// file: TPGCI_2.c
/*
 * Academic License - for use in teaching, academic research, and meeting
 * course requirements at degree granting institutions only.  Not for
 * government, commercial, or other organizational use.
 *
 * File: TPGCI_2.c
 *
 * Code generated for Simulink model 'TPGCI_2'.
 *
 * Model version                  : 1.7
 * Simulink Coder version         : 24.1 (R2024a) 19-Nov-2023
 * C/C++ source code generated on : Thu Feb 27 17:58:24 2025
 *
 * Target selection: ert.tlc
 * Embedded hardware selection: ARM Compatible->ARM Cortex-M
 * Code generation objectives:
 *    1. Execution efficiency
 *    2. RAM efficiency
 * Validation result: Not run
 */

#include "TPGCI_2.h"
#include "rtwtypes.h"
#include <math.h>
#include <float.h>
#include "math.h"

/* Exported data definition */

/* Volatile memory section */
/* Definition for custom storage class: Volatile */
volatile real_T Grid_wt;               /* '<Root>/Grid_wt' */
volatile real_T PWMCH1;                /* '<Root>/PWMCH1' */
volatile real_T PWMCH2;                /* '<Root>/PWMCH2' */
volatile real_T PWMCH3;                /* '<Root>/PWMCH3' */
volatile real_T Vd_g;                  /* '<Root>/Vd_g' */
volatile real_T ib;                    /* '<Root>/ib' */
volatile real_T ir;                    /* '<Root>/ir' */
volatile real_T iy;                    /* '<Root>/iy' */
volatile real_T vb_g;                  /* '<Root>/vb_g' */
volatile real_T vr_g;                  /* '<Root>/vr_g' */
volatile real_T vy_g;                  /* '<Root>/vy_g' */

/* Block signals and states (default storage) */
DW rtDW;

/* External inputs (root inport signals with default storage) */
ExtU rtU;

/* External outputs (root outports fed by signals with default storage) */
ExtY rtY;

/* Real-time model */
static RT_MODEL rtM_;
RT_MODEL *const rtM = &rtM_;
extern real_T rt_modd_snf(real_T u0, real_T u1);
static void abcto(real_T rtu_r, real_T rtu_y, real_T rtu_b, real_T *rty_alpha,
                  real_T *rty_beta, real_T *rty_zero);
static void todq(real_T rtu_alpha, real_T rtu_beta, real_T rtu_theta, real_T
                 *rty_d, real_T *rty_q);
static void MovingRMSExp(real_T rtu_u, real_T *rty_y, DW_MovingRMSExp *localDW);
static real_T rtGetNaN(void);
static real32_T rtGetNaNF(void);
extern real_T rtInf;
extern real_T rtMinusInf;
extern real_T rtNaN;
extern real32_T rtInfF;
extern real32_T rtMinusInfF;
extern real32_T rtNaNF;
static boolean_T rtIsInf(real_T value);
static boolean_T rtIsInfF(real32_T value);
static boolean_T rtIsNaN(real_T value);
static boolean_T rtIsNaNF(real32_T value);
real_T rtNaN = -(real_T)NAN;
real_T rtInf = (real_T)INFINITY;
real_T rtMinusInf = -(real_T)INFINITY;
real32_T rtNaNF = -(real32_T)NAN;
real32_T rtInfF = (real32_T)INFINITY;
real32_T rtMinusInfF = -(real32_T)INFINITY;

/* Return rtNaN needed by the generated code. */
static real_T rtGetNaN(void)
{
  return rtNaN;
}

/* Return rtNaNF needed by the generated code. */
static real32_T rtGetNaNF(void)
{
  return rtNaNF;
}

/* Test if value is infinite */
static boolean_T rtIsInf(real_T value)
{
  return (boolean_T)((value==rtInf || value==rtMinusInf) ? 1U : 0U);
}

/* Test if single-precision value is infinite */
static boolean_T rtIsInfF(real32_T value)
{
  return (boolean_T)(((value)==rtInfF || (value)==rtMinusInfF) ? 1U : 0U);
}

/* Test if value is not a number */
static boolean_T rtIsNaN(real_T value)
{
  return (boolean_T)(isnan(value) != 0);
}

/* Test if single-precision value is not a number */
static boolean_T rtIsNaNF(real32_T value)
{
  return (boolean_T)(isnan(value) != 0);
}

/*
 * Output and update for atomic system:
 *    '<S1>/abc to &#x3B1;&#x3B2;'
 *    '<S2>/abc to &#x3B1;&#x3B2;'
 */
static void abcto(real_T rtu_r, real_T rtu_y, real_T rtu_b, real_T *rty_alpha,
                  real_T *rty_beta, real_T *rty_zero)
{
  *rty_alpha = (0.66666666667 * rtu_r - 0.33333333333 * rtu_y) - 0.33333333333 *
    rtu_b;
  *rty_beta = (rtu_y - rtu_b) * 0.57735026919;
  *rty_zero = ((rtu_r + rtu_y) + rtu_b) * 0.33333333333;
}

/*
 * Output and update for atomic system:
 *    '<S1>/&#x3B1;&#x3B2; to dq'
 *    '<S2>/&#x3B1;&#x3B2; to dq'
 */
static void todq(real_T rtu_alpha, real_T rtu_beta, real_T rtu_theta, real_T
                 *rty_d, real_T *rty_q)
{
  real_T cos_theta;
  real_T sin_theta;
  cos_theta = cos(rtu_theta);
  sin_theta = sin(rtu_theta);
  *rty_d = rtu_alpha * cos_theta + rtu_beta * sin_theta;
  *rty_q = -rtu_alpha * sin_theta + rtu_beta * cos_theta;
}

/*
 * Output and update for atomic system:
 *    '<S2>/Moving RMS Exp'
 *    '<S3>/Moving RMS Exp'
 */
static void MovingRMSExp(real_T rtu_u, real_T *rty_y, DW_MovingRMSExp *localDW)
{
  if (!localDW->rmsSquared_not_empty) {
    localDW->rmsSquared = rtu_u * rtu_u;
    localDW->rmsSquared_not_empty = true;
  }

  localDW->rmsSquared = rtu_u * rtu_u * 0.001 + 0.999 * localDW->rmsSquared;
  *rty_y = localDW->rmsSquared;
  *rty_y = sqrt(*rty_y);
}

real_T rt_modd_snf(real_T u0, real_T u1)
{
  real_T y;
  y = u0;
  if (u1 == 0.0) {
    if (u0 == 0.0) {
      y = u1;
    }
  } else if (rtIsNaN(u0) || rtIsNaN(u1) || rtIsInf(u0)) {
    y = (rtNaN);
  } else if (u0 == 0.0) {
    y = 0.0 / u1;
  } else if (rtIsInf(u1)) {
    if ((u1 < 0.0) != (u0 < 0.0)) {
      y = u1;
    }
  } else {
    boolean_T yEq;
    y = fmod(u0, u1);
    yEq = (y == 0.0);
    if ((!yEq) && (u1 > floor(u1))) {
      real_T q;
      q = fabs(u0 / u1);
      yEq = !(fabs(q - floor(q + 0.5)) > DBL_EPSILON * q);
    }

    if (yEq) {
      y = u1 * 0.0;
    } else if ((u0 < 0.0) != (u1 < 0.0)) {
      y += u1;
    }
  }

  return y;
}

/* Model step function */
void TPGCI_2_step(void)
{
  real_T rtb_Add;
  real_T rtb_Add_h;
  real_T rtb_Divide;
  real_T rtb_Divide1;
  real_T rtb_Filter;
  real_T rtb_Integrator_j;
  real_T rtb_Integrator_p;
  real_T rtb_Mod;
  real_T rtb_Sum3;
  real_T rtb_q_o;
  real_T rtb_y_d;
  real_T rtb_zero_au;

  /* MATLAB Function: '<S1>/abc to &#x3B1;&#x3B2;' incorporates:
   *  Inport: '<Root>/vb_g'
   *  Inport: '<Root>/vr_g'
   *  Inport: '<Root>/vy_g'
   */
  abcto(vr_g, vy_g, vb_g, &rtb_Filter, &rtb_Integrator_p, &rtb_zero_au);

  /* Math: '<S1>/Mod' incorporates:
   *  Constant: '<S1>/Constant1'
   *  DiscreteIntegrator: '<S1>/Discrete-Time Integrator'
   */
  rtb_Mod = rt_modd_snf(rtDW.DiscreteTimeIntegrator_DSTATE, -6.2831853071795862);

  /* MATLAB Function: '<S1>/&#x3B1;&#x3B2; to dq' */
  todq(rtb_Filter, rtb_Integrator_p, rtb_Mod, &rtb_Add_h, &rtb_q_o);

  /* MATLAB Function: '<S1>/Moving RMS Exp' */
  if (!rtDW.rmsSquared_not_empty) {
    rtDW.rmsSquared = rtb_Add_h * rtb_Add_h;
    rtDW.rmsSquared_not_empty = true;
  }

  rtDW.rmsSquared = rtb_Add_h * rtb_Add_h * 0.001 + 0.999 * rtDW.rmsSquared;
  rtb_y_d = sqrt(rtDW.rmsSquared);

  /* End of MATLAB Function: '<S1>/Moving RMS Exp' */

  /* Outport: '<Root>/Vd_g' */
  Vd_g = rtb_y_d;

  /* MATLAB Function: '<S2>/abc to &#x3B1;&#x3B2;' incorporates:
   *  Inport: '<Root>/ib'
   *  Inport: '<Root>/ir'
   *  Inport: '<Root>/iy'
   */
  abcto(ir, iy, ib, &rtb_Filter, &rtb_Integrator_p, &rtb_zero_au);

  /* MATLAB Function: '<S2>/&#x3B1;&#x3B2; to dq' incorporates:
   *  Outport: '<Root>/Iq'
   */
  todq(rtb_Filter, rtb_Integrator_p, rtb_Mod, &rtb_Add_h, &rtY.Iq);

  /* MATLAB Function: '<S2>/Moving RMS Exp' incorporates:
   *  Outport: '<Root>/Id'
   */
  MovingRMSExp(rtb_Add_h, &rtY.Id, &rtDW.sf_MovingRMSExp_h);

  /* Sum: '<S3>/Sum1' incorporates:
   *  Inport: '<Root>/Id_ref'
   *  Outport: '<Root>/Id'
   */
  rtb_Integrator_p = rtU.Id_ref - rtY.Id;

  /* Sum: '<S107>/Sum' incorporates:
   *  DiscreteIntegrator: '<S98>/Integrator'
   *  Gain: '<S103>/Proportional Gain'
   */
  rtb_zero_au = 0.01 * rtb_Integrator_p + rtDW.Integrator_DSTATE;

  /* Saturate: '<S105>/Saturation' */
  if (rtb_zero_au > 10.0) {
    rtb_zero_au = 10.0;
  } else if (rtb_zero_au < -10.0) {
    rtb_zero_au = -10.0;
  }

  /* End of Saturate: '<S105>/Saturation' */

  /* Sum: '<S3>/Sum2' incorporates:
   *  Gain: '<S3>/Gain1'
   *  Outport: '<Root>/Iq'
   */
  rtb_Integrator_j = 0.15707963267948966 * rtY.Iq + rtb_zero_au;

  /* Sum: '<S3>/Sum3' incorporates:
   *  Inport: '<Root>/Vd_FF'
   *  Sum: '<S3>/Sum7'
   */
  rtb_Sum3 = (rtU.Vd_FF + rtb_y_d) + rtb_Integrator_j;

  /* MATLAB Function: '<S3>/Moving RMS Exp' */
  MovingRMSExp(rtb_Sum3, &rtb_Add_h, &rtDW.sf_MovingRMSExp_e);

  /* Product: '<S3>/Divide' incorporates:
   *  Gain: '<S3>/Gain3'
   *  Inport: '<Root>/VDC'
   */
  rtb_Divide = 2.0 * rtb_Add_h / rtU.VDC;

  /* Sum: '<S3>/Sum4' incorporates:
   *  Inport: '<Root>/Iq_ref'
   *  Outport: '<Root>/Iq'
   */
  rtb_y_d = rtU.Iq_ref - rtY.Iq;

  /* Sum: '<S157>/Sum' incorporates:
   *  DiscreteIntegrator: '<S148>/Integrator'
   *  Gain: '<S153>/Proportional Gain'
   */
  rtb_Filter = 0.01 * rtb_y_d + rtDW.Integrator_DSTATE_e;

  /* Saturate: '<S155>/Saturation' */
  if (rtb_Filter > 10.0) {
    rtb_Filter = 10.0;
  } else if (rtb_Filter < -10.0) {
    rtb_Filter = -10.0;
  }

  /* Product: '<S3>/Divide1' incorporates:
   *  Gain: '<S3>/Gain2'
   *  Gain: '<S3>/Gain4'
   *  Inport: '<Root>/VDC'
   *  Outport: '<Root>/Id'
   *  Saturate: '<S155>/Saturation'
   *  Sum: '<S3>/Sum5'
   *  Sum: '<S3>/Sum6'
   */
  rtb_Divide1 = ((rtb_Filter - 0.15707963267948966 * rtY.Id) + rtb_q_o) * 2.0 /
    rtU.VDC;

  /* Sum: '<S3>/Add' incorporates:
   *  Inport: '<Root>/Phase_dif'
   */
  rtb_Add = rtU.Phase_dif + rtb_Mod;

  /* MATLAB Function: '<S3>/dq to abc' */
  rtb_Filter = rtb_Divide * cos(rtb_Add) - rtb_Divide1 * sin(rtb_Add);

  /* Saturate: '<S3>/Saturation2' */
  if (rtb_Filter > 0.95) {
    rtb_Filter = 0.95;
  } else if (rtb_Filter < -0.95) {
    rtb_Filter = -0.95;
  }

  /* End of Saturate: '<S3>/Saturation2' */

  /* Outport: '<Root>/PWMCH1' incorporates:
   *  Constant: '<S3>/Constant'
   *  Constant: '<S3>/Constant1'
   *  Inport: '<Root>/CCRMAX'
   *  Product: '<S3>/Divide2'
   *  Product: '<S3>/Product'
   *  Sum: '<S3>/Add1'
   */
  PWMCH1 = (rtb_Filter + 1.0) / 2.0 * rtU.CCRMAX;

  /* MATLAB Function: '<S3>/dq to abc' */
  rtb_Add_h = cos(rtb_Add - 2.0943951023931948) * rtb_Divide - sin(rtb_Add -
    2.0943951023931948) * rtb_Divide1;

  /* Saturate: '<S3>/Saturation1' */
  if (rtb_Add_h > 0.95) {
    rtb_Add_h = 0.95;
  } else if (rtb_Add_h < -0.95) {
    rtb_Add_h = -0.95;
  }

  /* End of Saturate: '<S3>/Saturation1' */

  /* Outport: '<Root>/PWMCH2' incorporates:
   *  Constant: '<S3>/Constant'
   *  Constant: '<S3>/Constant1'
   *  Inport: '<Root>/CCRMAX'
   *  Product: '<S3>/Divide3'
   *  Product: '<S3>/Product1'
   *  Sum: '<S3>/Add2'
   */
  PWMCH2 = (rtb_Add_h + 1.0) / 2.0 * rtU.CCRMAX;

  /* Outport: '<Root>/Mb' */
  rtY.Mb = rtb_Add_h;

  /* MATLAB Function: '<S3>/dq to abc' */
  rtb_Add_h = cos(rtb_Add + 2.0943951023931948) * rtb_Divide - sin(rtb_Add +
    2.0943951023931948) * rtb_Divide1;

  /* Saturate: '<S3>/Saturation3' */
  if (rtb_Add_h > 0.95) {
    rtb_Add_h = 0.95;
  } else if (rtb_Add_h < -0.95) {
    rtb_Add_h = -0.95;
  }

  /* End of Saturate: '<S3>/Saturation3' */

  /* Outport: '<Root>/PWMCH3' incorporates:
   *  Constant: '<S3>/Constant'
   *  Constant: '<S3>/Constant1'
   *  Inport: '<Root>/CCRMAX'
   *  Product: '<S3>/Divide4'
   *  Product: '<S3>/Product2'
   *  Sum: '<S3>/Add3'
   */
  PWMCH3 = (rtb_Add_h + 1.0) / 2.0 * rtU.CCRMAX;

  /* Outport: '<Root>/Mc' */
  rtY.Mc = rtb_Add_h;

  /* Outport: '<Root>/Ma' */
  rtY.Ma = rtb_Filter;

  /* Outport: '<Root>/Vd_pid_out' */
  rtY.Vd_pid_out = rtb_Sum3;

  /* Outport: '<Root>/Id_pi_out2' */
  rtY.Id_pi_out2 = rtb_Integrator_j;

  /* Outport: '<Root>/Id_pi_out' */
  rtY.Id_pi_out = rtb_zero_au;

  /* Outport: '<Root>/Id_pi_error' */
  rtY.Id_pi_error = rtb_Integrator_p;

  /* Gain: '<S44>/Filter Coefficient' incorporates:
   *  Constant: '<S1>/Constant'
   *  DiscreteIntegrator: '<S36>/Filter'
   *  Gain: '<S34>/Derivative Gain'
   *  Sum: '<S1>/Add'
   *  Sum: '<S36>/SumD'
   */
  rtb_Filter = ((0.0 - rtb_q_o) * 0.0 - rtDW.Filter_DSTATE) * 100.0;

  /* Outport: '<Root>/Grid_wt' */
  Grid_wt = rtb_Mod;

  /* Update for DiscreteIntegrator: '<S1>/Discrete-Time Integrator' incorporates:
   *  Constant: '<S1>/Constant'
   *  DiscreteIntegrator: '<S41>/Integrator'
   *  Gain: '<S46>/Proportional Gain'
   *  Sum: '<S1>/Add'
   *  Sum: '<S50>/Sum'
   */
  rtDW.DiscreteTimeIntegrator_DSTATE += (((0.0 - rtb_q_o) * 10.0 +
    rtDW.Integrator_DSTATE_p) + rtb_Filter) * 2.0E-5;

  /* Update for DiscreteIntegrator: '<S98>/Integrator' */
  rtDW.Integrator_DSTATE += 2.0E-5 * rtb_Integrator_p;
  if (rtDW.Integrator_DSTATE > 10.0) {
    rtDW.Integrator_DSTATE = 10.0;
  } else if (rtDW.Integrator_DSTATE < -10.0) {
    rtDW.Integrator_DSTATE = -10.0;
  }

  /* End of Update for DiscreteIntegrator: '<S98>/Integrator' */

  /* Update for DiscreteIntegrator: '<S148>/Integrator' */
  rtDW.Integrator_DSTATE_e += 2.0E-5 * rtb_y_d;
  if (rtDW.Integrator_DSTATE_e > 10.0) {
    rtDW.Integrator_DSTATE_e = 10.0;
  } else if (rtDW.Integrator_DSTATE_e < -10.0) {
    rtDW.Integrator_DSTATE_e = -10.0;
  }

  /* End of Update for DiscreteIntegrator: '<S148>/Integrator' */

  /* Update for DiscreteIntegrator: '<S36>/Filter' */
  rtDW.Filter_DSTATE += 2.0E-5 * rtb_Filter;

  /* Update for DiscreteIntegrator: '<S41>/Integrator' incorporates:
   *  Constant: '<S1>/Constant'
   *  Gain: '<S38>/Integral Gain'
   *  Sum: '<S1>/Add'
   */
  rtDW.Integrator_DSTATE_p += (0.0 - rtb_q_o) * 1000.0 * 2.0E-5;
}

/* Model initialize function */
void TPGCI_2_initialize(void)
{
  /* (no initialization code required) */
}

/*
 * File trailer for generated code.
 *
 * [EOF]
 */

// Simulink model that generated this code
simulink model "TPGCI_2"  (R2024a)
settings: Solver=FixedStepDiscrete  StartTime=0.0  StopTime=10.0  FixedStep=2e-5  RelTol=1e-3
undefined symbols (not defined in the file): DiscIntNeverNeededParam
libraries: slpidlib x3

== system TPGCI_2 ==
  vr_g : Inport
  vy_g : Inport  Port=2
  vb_g : Inport  Port=3
  ir : Inport  Port=4
  iy : Inport  Port=5
  ib : Inport  Port=6
  Id_ref : Inport  Port=7
  Iq_ref : Inport  Port=8
  VDC : Inport  Port=9
  Phase_dif : Inport  Port=10
  Vd_FF : Inport  Port=11
  CCRMAX : Inport  Port=12
  Phase locked loop : Subsystem
  Subsystem : Subsystem
  Subsystem1 : Subsystem
  Vd_g : Outport
  Grid_wt : Outport  Port=2
  Id : Outport  Port=3
  Iq : Outport  Port=4
  PWMCH1 : Outport  Port=5
  PWMCH2 : Outport  Port=6
  PWMCH3 : Outport  Port=7
  Ma : Outport  Port=8
  Mb : Outport  Port=9
  Mc : Outport  Port=10
  Vd_pid_out : Outport  Port=11
  Id_pi_error : Outport  Port=12
  Id_pi_out : Outport  Port=13
  Id_pi_out2 : Outport  Port=14
  wires:
  Iq_ref/1 -> Subsystem1/2(Iq_ref)
  Vd_FF/1 -> Subsystem1/5(Vd_FF)
  Subsystem/1(Id) -> Id/1
  VDC/1 -> Subsystem1/3(VDC)
  vy_g/1 -> Phase locked loop/2(vy_g)
  Phase locked loop/2(wt) -> Grid_wt/1
  ir/1 -> Subsystem/1(r)
  ib/1 -> Subsystem/3(b)
  vb_g/1 -> Phase locked loop/3(vb_g)
  Phase_dif/1 -> Subsystem1/4(Phase_dif)
  iy/1 -> Subsystem/2(y)
  Id_ref/1 -> Subsystem1/1(Id_ref)
  vr_g/1 -> Phase locked loop/1(vr_g)
  Subsystem/2(Iq) -> Iq/1
  Phase locked loop/1(Vd_g) -> Vd_g/1
  CCRMAX/1 -> Subsystem1/6(CCRMAX)
  Subsystem1/1(Vd_pid_out) -> Vd_pid_out/1
  Subsystem1/2(Id_pi_error) -> Id_pi_error/1
  Subsystem1/3(Id_pi_out) -> Id_pi_out/1
  Subsystem1/4(Id_pi_out2) -> Id_pi_out2/1
  Subsystem1/5(PWMCH1) -> PWMCH1/1
  Subsystem1/6(PWMCH2) -> PWMCH2/1
  Subsystem1/7(PWMCH3) -> PWMCH3/1
  Subsystem1/8(Ma) -> Ma/1
  Subsystem1/9(Mb) -> Mb/1
  Subsystem1/10(Mc) -> Mc/1

== system TPGCI_2/Phase locked loop ==
  vr_g : Inport
  vy_g : Inport  Port=2
  vb_g : Inport  Port=3
  Add : Sum  Inputs=+-
  Constant : Constant  Value=0
  Constant1 : Constant  Value=-2*pi
  Discrete-Time Integrator : DiscreteIntegrator  SampleTime=2e-5  ICPrevOutput=DiscIntNeverNeededParam  ICPrevScaledInput=DiscIntNeverNeededParam
  Mod : Math  Operator=mod
  Moving RMS Exp : MATLAB Function  TreatAsAtomicUnit=on
  PID Controller : slpidlib/PID Controller  Controller=PID  Form=Parallel  TimeDomain=Discrete-time  UseExternalTs=off  SampleTime=2e-5  IntegratorMethod=Forward Euler  FilterMethod=Forward Euler  ControllerParametersSource=internal  P=10  I=1000  UseKiTs=off  D=0  UseExternalDerivativeSource=off  N=100  UseFilter=on  TunerSelectOption=Transfer Function Based (PID Tuner App)  InitialConditionSource=internal  InitialConditionForIntegrator=0  InitialConditionForFilter=0  DifferentiatorICPrevScaledInput=0  ExternalReset=none  TrackingMode=off  Kt=1  LimitOutput=off  SatLimitsSource=internal  UpperSaturationLimit=inf  LowerSaturationLimit=-inf  LinearizeAsGain=on  AntiWindupMode=none  Kb=1  LimitIntegrator=off  UpperIntegratorSaturationLimit=inf  LowerIntegratorSaturationLimit=-inf  POutMin=[]  POutMax=[]  IOutMin=[]  IOutMax=[]  DOutMin=[]  DOutMax=[]  NOutMin=[]  NOutMax=[]  SumOutMin=[]  SumOutMax=[]  SaturationOutMin=[]  SaturationOutMax=[]  PParamMin=[]  PParamMax=[]  IParamMin=[]  IParamMax=[]  DParamMin=[]  DParamMax=[]  NParamMin=[]  NParamMax=[]  KbParamMin=[]  KbParamMax=[]  KtParamMin=[]  KtParamMax=[]  KbOutMin=[]  KbOutMax=[]  KtOutMin=[]  KtOutMax=[]  IntegratorOutMin=[]  IntegratorOutMax=[]  FilterOutMin=[]  FilterOutMax=[]  SumI1OutMin=[]  SumI1OutMax=[]  SumI2OutMin=[]  SumI2OutMax=[]  SumI3OutMin=[]  SumI3OutMax=[]  SumI4OutMin=[]  SumI4OutMax=[]  SumDOutMin=[]  SumDOutMax=[]  DifferentiatorOutMin=[]  DifferentiatorOutMax=[]  FilterDiffOutCoefMin=[]  FilterDiffOutCoefMax=[]  ReciprocalOutMin=[]  ReciprocalOutMax=[]  SumDenOutMin=[]  SumDenOutMax=[]  SumNumOutMin=[]  SumNumOutMax=[]  DivideOutMin=[]  DivideOutMax=[]  UdiffTsProdOutMin=[]  UdiffTsProdOutMax=[]  NTsProdOutMin=[]  NTsProdOutMax=[]  UintegralTsProdOutMin=[]  UintegralTsProdOutMax=[]  UngainTsProdOutMin=[]  UngainTsProdOutMax=[]  ClampingZeroOutDataTypeStr=Inherit: Inherit via back propagation  ClampingZeroOutMin=[]  ClampingZeroOutMax=[]  FilterDenConstantOutDataTypeStr=Inherit: Inherit via back propagation  FilterDenConstantOutMin=[]  FilterDenConstantOutMax=[]  PCopyOutDataTypeStr=Inherit: Inherit via back propagation  PCopyOutMin=[]  PCopyOutMax=[]  NCopyOutDataTypeStr=Inherit: Inherit via back propagation  NCopyOutMin=[]  NCopyOutMax=[]  IntegratorContinuousStateAttributes=''  IntegratorStateMustResolveToSignalObject=off  IntegratorRTWStateStorageClass=Auto  FilterContinuousStateAttributes=''  FilterStateMustResolveToSignalObject=off  FilterRTWStateStorageClass=Auto  ParallelPVariant=InternalParameters  IdealPVariant=Disabled  IVariant=InternalParameters  DVariant=InternalParameters  IntegratorVariant=Discrete  SatVariant=Disabled  AWVariant=Passthrough  PCopyVariant=Disabled  TRVariant=Disabled  FdbkBlocksVariant=Forward  IdealPFdbkVariant=Disabled  SatFdbkVariant=Disabled  DerivativeFilterVariant=ForwardEulerFilter  NVariant=InternalParameters  NCopyVariant=Disabled  FilterICVariant=InternalICsFilter  IntegratorICVariant=InternalICs  ExternalResetVariant=Disabled  TRSumVariant=Passthrough  SumFdbkVariant=Disabled  SumVariant=Sum_PID  TsampFilterVariant=InternalTs  TsampNgainVariant=Passthrough  TsampIntegralVariant=Disabled_SignalSpec  ExternalSaturationOutDataTypeStr=Inherit: Same as second input  DerivativeSourceVariant=ErrorSignal
  Terminator1 : Terminator
  abc to αβ : MATLAB Function  TreatAsAtomicUnit=on
  αβ to dq : MATLAB Function  TreatAsAtomicUnit=on
  Vd_g : Outport
  wt : Outport  Port=2
  tag scope: Vd_g=global, Vq_g=global, wt=global
  wires:
  αβ to dq/3(zero) -> Terminator1/1
  abc to αβ/2(beta) -> αβ to dq/2(beta)
  αβ to dq/1(d) -> Moving RMS Exp/1(u)
  [wt] -> αβ to dq/4(theta)
  abc to αβ/1(alpha) -> αβ to dq/1(alpha)
  abc to αβ/3(zero) -> αβ to dq/3("zero ")
  Mod/1 -> wt/1, [wt]
  Discrete-Time Integrator/1 -> Mod/1
  Constant1/1 -> Mod/2
  Constant/1 -> Add/1
  αβ to dq/2(q) -> [Vq_g], Add/2
  PID Controller/1 -> Discrete-Time Integrator/1
  Add/1 -> PID Controller/1
  vy_g/1 -> abc to αβ/2(y)
  vb_g/1 -> abc to αβ/3(b)
  vr_g/1 -> abc to αβ/1(r)
  Moving RMS Exp/1(y) -> [Vd_g], Vd_g/1

== system TPGCI_2/Subsystem ==
  r : Inport
  y : Inport  Port=2
  b : Inport  Port=3
  Moving RMS Exp : MATLAB Function  TreatAsAtomicUnit=on
  Terminator1 : Terminator
  abc to αβ : MATLAB Function  TreatAsAtomicUnit=on
  αβ to dq : MATLAB Function  TreatAsAtomicUnit=on
  Id : Outport
  Iq : Outport  Port=2
  tag scope: Id_i=global, Iq_i=global
  wires:
  abc to αβ/2(beta) -> αβ to dq/2(beta)
  αβ to dq/1(d) -> Moving RMS Exp/1(u)
  αβ to dq/2(q) -> Iq/1, [Iq_i]
  abc to αβ/1(alpha) -> αβ to dq/1(alpha)
  abc to αβ/3(zero) -> αβ to dq/3("zero ")
  αβ to dq/3(zero) -> Terminator1/1
  Moving RMS Exp/1(y) -> Id/1, [Id_i]
  [wt] -> αβ to dq/4(theta)
  y/1 -> abc to αβ/2(y)
  b/1 -> abc to αβ/3(b)
  r/1 -> abc to αβ/1(r)

== system TPGCI_2/Subsystem1 ==
  note: Iq Reference
  note: Id Reference
  Id_ref : Inport
  Iq_ref : Inport  Port=2
  VDC : Inport  Port=3
  Phase_dif : Inport  Port=4
  Vd_FF : Inport  Port=5
  CCRMAX : Inport  Port=6
  Add{,1..3} (4 alike) : Sum
  Constant : Constant
  Constant1 : Constant  Value=2  VectorParams1D=off  SampleTime=-1
  Divide{,1..4} (5 alike) : Product  Inputs=*/
  Gain1 : Gain  Gain=2*pi*50*500e-6
  Gain2 : Gain  Gain=2*pi*50*500e-6
  Gain3 : Gain  Gain=2
  Gain4 : Gain  Gain=2
  Moving RMS Exp : MATLAB Function  TreatAsAtomicUnit=on
  PID Controller1 : slpidlib/PID Controller  Controller=PI  Form=Parallel  TimeDomain=Discrete-time  UseExternalTs=off  SampleTime=2e-5  IntegratorMethod=Forward Euler  FilterMethod=Forward Euler  ControllerParametersSource=internal  P=0.01  I=1  UseKiTs=off  D=0  UseExternalDerivativeSource=off  N=100  UseFilter=on  TunerSelectOption=Transfer Function Based (PID Tuner App)  InitialConditionSource=internal  InitialConditionForIntegrator=0  InitialConditionForFilter=0  DifferentiatorICPrevScaledInput=0  ExternalReset=none  TrackingMode=off  Kt=1  LimitOutput=on  SatLimitsSource=internal  UpperSaturationLimit=+10  LowerSaturationLimit=-10  LinearizeAsGain=on  AntiWindupMode=none  Kb=1  LimitIntegrator=on  UpperIntegratorSaturationLimit=+10  LowerIntegratorSaturationLimit=-10  RndMeth=Nearest  POutMin=[]  POutMax=[]  IOutMin=[]  IOutMax=[]  DOutMin=[]  DOutMax=[]  NOutMin=[]  NOutMax=[]  SumOutMin=[]  SumOutMax=[]  SaturationOutMin=[]  SaturationOutMax=[]  PParamMin=[]  PParamMax=[]  IParamMin=[]  IParamMax=[]  DParamMin=[]  DParamMax=[]  NParamMin=[]  NParamMax=[]  KbParamMin=[]  KbParamMax=[]  KtParamMin=[]  KtParamMax=[]  KbOutMin=[]  KbOutMax=[]  KtOutMin=[]  KtOutMax=[]  IntegratorOutMin=[]  IntegratorOutMax=[]  FilterOutMin=[]  FilterOutMax=[]  SumI1OutMin=[]  SumI1OutMax=[]  SumI2OutMin=[]  SumI2OutMax=[]  SumI3OutMin=[]  SumI3OutMax=[]  SumI4OutMin=[]  SumI4OutMax=[]  SumDOutMin=[]  SumDOutMax=[]  DifferentiatorOutMin=[]  DifferentiatorOutMax=[]  FilterDiffOutCoefMin=[]  FilterDiffOutCoefMax=[]  ReciprocalOutMin=[]  ReciprocalOutMax=[]  SumDenOutMin=[]  SumDenOutMax=[]  SumNumOutMin=[]  SumNumOutMax=[]  DivideOutMin=[]  DivideOutMax=[]  UdiffTsProdOutMin=[]  UdiffTsProdOutMax=[]  NTsProdOutMin=[]  NTsProdOutMax=[]  UintegralTsProdOutMin=[]  UintegralTsProdOutMax=[]  UngainTsProdOutMin=[]  UngainTsProdOutMax=[]  ClampingZeroOutDataTypeStr=Inherit: Inherit via back propagation  ClampingZeroOutMin=[]  ClampingZeroOutMax=[]  FilterDenConstantOutDataTypeStr=Inherit: Inherit via back propagation  FilterDenConstantOutMin=[]  FilterDenConstantOutMax=[]  PCopyOutDataTypeStr=Inherit: Inherit via back propagation  PCopyOutMin=[]  PCopyOutMax=[]  NCopyOutDataTypeStr=Inherit: Inherit via back propagation  NCopyOutMin=[]  NCopyOutMax=[]  IntegratorContinuousStateAttributes=''  IntegratorStateMustResolveToSignalObject=off  IntegratorRTWStateStorageClass=Auto  FilterContinuousStateAttributes=''  FilterStateMustResolveToSignalObject=off  FilterRTWStateStorageClass=Auto  ParallelPVariant=InternalParameters  IdealPVariant=Disabled  IVariant=InternalParameters  DVariant=Disabled  IntegratorVariant=Discrete  SatVariant=Enabled  AWVariant=Passthrough  PCopyVariant=Disabled  TRVariant=Disabled  FdbkBlocksVariant=Forward  IdealPFdbkVariant=Disabled  SatFdbkVariant=Disabled  DerivativeFilterVariant=Disabled  NVariant=Disabled  NCopyVariant=Disabled_SignalSpec  FilterICVariant=Disabled  IntegratorICVariant=InternalICs  ExternalResetVariant=Disabled  TRSumVariant=Passthrough  SumFdbkVariant=Disabled  SumVariant=Sum_PI  TsampFilterVariant=InternalTs  TsampNgainVariant=Passthrough  TsampIntegralVariant=Disabled_SignalSpec  ExternalSaturationOutDataTypeStr=Inherit: Same as second input  DerivativeSourceVariant=Disabled
  PID Controller2 : slpidlib/PID Controller  Controller=PI  Form=Parallel  TimeDomain=Discrete-time  UseExternalTs=off  SampleTime=2e-5  IntegratorMethod=Forward Euler  FilterMethod=Forward Euler  ControllerParametersSource=internal  P=0.01  I=1  UseKiTs=off  D=0  UseExternalDerivativeSource=off  N=100  UseFilter=on  TunerSelectOption=Transfer Function Based (PID Tuner App)  InitialConditionSource=internal  InitialConditionForIntegrator=0  InitialConditionForFilter=0  DifferentiatorICPrevScaledInput=0  ExternalReset=none  TrackingMode=off  Kt=1  LimitOutput=on  SatLimitsSource=internal  UpperSaturationLimit=10  LowerSaturationLimit=-10  LinearizeAsGain=on  AntiWindupMode=none  Kb=1  LimitIntegrator=on  UpperIntegratorSaturationLimit=10  LowerIntegratorSaturationLimit=-10  POutMin=[]  POutMax=[]  IOutMin=[]  IOutMax=[]  DOutMin=[]  DOutMax=[]  NOutMin=[]  NOutMax=[]  SumOutMin=[]  SumOutMax=[]  SaturationOutMin=[]  SaturationOutMax=[]  PParamMin=[]  PParamMax=[]  IParamMin=[]  IParamMax=[]  DParamMin=[]  DParamMax=[]  NParamMin=[]  NParamMax=[]  KbParamMin=[]  KbParamMax=[]  KtParamMin=[]  KtParamMax=[]  KbOutMin=[]  KbOutMax=[]  KtOutMin=[]  KtOutMax=[]  IntegratorOutMin=[]  IntegratorOutMax=[]  FilterOutMin=[]  FilterOutMax=[]  SumI1OutMin=[]  SumI1OutMax=[]  SumI2OutMin=[]  SumI2OutMax=[]  SumI3OutMin=[]  SumI3OutMax=[]  SumI4OutMin=[]  SumI4OutMax=[]  SumDOutMin=[]  SumDOutMax=[]  DifferentiatorOutMin=[]  DifferentiatorOutMax=[]  FilterDiffOutCoefMin=[]  FilterDiffOutCoefMax=[]  ReciprocalOutMin=[]  ReciprocalOutMax=[]  SumDenOutMin=[]  SumDenOutMax=[]  SumNumOutMin=[]  SumNumOutMax=[]  DivideOutMin=[]  DivideOutMax=[]  UdiffTsProdOutMin=[]  UdiffTsProdOutMax=[]  NTsProdOutMin=[]  NTsProdOutMax=[]  UintegralTsProdOutMin=[]  UintegralTsProdOutMax=[]  UngainTsProdOutMin=[]  UngainTsProdOutMax=[]  ClampingZeroOutDataTypeStr=Inherit: Inherit via back propagation  ClampingZeroOutMin=[]  ClampingZeroOutMax=[]  FilterDenConstantOutDataTypeStr=Inherit: Inherit via back propagation  FilterDenConstantOutMin=[]  FilterDenConstantOutMax=[]  PCopyOutDataTypeStr=Inherit: Inherit via back propagation  PCopyOutMin=[]  PCopyOutMax=[]  NCopyOutDataTypeStr=Inherit: Inherit via back propagation  NCopyOutMin=[]  NCopyOutMax=[]  IntegratorContinuousStateAttributes=''  IntegratorStateMustResolveToSignalObject=off  IntegratorRTWStateStorageClass=Auto  FilterContinuousStateAttributes=''  FilterStateMustResolveToSignalObject=off  FilterRTWStateStorageClass=Auto  ParallelPVariant=InternalParameters  IdealPVariant=Disabled  IVariant=InternalParameters  DVariant=Disabled  IntegratorVariant=Discrete  SatVariant=Enabled  AWVariant=Passthrough  PCopyVariant=Disabled  TRVariant=Disabled  FdbkBlocksVariant=Forward  IdealPFdbkVariant=Disabled  SatFdbkVariant=Disabled  DerivativeFilterVariant=Disabled  NVariant=Disabled  NCopyVariant=Disabled_SignalSpec  FilterICVariant=Disabled  IntegratorICVariant=InternalICs  ExternalResetVariant=Disabled  TRSumVariant=Passthrough  SumFdbkVariant=Disabled  SumVariant=Sum_PI  TsampFilterVariant=InternalTs  TsampNgainVariant=Passthrough  TsampIntegralVariant=Disabled_SignalSpec  ExternalSaturationOutDataTypeStr=Inherit: Same as second input  DerivativeSourceVariant=Disabled
  Product : Product
  Product1 : Product
  Product2 : Product
  Saturation1 : Saturate  UpperLimit=0.95  LowerLimit=-0.95
  Saturation2 : Saturate  UpperLimit=0.95  LowerLimit=-0.95
  Saturation3 : Saturate  UpperLimit=0.95  LowerLimit=-0.95
  Sum1 : Sum  Inputs=|+-
  Sum{2..3,6..7} (4 alike) : Sum  Inputs=|++
  Sum4 : Sum  Inputs=|+-
  Sum5 : Sum  Inputs=|+-
  dq to abc : MATLAB Function  TreatAsAtomicUnit=on
  Vd_pid_out : Outport
  Id_pi_error : Outport  Port=2
  Id_pi_out : Outport  Port=3
  Id_pi_out2 : Outport  Port=4
  PWMCH1 : Outport  Port=5
  PWMCH2 : Outport  Port=6
  PWMCH3 : Outport  Port=7
  Ma : Outport  Port=8
  Mb : Outport  Port=9
  Mc : Outport  Port=10
  tag scope: VDC=global, ma=global, mb=global, mc=global, md=global, mq=global
  wires:
  [Id_i] -> Gain2/1
  Sum4/1 -> PID Controller2/1
  Iq_ref/1 -> Sum4/1
  [Id_i] -> Sum1/2
  Sum2/1 -> Id_pi_out2/1, Sum3/1
  Sum3/1 -> Moving RMS Exp/1(u), Vd_pid_out/1
  PID Controller1/1 -> Id_pi_out/1, Sum2/1
  Gain1/1 -> Sum2/2
  Sum5/1 -> Sum6/1
  Sum1/1 -> Id_pi_error/1, PID Controller1/1
  PID Controller2/1 -> Sum5/1
  Gain2/1 -> Sum5/2
  [Vq_g] -> Sum6/2
  [Iq_i] -> Sum4/2
  [Iq_i] -> Gain1/1
  Id_ref/1 -> Sum1/1
  Add/1 -> dq to abc/3(theta)
  [wt] -> Add/2
  Phase_dif/1 -> Add/1
  Vd_FF/1 -> Sum7/1
  [Vd_g] -> Sum7/2
  Sum7/1 -> Sum3/2
  [VDC] -> Divide/2
  Divide/1 -> [md]
  Gain3/1 -> Divide/1
  Sum6/1 -> Gain4/1
  Divide1/1 -> [mq]
  Gain4/1 -> Divide1/1
  [VDC] -> Divide1/2
  [md] -> dq to abc/1(d)
  [mq] -> dq to abc/2(q)
  VDC/1 -> [VDC]
  Add1/1 -> Divide2/1
  [mc] -> Add3/1
  Constant/1 -> Add1/2, Add2/2, Add3/2
  [ma] -> Add1/1
  Add3/1 -> Divide4/1
  Add2/1 -> Divide3/1
  Divide4/1 -> Product2/1
  Divide3/1 -> Product1/1
  Constant1/1 -> Divide2/2, Divide3/2, Divide4/2
  CCRMAX/1 -> Product2/2, Product1/2, Product/2
  Product1/1 -> PWMCH2/1
  dq to abc/3(c) -> Saturation3/1
  dq to abc/1(a) -> Saturation2/1
  Saturation2/1 -> Ma/1, [ma]
  [mb] -> Add2/1
  Saturation3/1 -> Mc/1, [mc]
  Product2/1 -> PWMCH3/1
  Saturation1/1 -> Mb/1, [mb]
  Product/1 -> PWMCH1/1
  Divide2/1 -> Product/1
  dq to abc/2(b) -> Saturation1/1
  Moving RMS Exp/1(y) -> Gain3/1

== matlab function TPGCI_2/Phase locked loop/αβ to dq ==
function [d, q, zero] = alphabeta_to_dq(alpha, beta, zero, theta) 
%ALPHABETA_TO_DQ Converts αβ0 voltages to dq0 using Park Transform
% Inputs:
%   v_alpha - Alpha axis voltage
%   v_beta  - Beta axis voltage
%   v_zero  - Zero sequence voltage
%   theta   - Rotational angle (radians)
% Outputs:
%   v_d     - Direct axis voltage
%   v_q     - Quadrature axis voltage
%   v_zero  - Zero sequence voltage (unchanged)

    % Precompute sine and cosine for efficiency
    cos_theta = cos(theta);
    sin_theta = sin(theta);

    % Compute dq0 components
    d =  alpha * cos_theta + beta * sin_theta;
    q = -alpha * sin_theta + beta * cos_theta;
    % v_zero remains the same
end

== matlab function TPGCI_2/Phase locked loop/abc to αβ ==
function [alpha, beta, zero] = abc_to_alphabeta(r, y, b) 
%#codegen
%ABC_TO_ALPHABETA Converts three-phase (ABC) voltages to αβ0 (Clark Transform)
% Inputs:
%   vr_g - Phase R voltage
%   vy_g - Phase Y voltage
%   vb_g - Phase B voltage
% Outputs:
%   v_alpha_g - Alpha axis voltage
%   v_beta_g  - Beta axis voltage
%   v_zero    - Zero sequence voltage
    % Precompute constants (avoiding divisions)
    k1 = 0.66666666667;  % 2/3
    k2 = 0.33333333333;  % 1/3
    k3 = 0.57735026919;  % sqrt(3)/3

    % Compute αβ0 components using direct arithmetic
    alpha = k1 * r - k2 * y - k2 * b;
    beta  = k3 * (y - b);
    zero    = k2 * (r + y + b);
end

== matlab function TPGCI_2/Phase locked loop/Moving RMS Exp ==
function y = movingRMSExp(u)
    % y = movingRMSExp(u, alpha)
    % This function computes the exponential moving RMS of the input signal `u`.
    % The parameter `alpha` is the smoothing factor (0 < alpha <= 1).
    % A higher `alpha` gives more weight to recent values.

    % Persistent variables to maintain state between calls
    persistent rmsSquared

    % Initialize the exponential moving RMS on the first call
    if isempty(rmsSquared)
        rmsSquared = u^2; % Initialize with the square of the first value

    end

    % Update the exponentially weighted RMS squared
    rmsSquared = 0.001 * u^2 + (1 - 0.001) * rmsSquared;

    % Compute the RMS as the square root of the weighted sum
    y = sqrt(rmsSquared);
end

== matlab function TPGCI_2/Subsystem/abc to αβ ==
function [alpha, beta, zero] = abc_to_alphabeta(r, y, b) 
%#codegen
%ABC_TO_ALPHABETA Converts three-phase (ABC) voltages to αβ0 (Clark Transform)
% Inputs:
%   vr_g - Phase R voltage
%   vy_g - Phase Y voltage
%   vb_g - Phase B voltage
% Outputs:
%   v_alpha_g - Alpha axis voltage
%   v_beta_g  - Beta axis voltage
%   v_zero    - Zero sequence voltage
    % Precompute constants (avoiding divisions)
    k1 = 0.66666666667;  % 2/3
    k2 = 0.33333333333;  % 1/3
    k3 = 0.57735026919;  % sqrt(3)/3

    % Compute αβ0 components using direct arithmetic
    alpha = k1 * r - k2 * y - k2 * b;
    beta  = k3 * (y - b);
    zero    = k2 * (r + y + b);
end

== matlab function TPGCI_2/Subsystem/αβ to dq ==
function [d, q, zero] = alphabeta_to_dq(alpha, beta, zero, theta) 
%ALPHABETA_TO_DQ Converts αβ0 voltages to dq0 using Park Transform
% Inputs:
%   v_alpha - Alpha axis voltage
%   v_beta  - Beta axis voltage
%   v_zero  - Zero sequence voltage
%   theta   - Rotational angle (radians)
% Outputs:
%   v_d     - Direct axis voltage
%   v_q     - Quadrature axis voltage
%   v_zero  - Zero sequence voltage (unchanged)

    % Precompute sine and cosine for efficiency
    cos_theta = cos(theta);
    sin_theta = sin(theta);

    % Compute dq0 components
    d =  alpha * cos_theta + beta * sin_theta;
    q = -alpha * sin_theta + beta * cos_theta;
    % v_zero remains the same
end

== matlab function TPGCI_2/Subsystem/Moving RMS Exp ==
function y = movingRMSExp(u)
    % y = movingRMSExp(u, alpha)
    % This function computes the exponential moving RMS of the input signal `u`.
    % The parameter `alpha` is the smoothing factor (0 < alpha <= 1).
    % A higher `alpha` gives more weight to recent values.

    % Persistent variables to maintain state between calls
    persistent rmsSquared

    % Initialize the exponential moving RMS on the first call
    if isempty(rmsSquared)
        rmsSquared = u^2; % Initialize with the square of the first value
    end

    % Update the exponentially weighted RMS squared
    rmsSquared = 0.001 * u^2 + (1 - 0.001) * rmsSquared;

    % Compute the RMS as the square root of the weighted sum
    y = sqrt(rmsSquared);
end

== matlab function TPGCI_2/Subsystem1/dq to abc ==
function [a, b, c] = dq_to_abc(d, q, theta)
%#codegen
% Converts dq0 frame to abc (three-phase) frame.

% Constants (Precomputed for efficiency)
TWO_PI_OVER_3 = 2.094395102393195;  % 2*pi/3
NEG_TWO_PI_OVER_3 = -2.094395102393195; % -2*pi/3

% Precompute sine and cosine values for efficiency
cos_theta = cos(theta);
sin_theta = sin(theta);

% Compute phase voltages using precomputed angles
a = d * cos_theta - q * sin_theta;
b = d * cos(theta + NEG_TWO_PI_OVER_3) - q * sin(theta + NEG_TWO_PI_OVER_3);
c = d * cos(theta + TWO_PI_OVER_3) - q * sin(theta + TWO_PI_OVER_3);

end

== matlab function TPGCI_2/Subsystem1/Moving RMS Exp ==
function y = movingRMSExp(u)
    % y = movingRMSExp(u, alpha)
    % This function computes the exponential moving RMS of the input signal `u`.
    % The parameter `alpha` is the smoothing factor (0 < alpha <= 1).
    % A higher `alpha` gives more weight to recent values.

    % Persistent variables to maintain state between calls
    persistent rmsSquared

    % Initialize the exponential moving RMS on the first call
    if isempty(rmsSquared)
        rmsSquared = u^2; % Initialize with the square of the first value
    end

    % Update the exponentially weighted RMS squared
    rmsSquared = 0.001 * u^2 + (1 - 0.001) * rmsSquared;

    % Compute the RMS as the square root of the weighted sum
    y = sqrt(rmsSquared);
end
